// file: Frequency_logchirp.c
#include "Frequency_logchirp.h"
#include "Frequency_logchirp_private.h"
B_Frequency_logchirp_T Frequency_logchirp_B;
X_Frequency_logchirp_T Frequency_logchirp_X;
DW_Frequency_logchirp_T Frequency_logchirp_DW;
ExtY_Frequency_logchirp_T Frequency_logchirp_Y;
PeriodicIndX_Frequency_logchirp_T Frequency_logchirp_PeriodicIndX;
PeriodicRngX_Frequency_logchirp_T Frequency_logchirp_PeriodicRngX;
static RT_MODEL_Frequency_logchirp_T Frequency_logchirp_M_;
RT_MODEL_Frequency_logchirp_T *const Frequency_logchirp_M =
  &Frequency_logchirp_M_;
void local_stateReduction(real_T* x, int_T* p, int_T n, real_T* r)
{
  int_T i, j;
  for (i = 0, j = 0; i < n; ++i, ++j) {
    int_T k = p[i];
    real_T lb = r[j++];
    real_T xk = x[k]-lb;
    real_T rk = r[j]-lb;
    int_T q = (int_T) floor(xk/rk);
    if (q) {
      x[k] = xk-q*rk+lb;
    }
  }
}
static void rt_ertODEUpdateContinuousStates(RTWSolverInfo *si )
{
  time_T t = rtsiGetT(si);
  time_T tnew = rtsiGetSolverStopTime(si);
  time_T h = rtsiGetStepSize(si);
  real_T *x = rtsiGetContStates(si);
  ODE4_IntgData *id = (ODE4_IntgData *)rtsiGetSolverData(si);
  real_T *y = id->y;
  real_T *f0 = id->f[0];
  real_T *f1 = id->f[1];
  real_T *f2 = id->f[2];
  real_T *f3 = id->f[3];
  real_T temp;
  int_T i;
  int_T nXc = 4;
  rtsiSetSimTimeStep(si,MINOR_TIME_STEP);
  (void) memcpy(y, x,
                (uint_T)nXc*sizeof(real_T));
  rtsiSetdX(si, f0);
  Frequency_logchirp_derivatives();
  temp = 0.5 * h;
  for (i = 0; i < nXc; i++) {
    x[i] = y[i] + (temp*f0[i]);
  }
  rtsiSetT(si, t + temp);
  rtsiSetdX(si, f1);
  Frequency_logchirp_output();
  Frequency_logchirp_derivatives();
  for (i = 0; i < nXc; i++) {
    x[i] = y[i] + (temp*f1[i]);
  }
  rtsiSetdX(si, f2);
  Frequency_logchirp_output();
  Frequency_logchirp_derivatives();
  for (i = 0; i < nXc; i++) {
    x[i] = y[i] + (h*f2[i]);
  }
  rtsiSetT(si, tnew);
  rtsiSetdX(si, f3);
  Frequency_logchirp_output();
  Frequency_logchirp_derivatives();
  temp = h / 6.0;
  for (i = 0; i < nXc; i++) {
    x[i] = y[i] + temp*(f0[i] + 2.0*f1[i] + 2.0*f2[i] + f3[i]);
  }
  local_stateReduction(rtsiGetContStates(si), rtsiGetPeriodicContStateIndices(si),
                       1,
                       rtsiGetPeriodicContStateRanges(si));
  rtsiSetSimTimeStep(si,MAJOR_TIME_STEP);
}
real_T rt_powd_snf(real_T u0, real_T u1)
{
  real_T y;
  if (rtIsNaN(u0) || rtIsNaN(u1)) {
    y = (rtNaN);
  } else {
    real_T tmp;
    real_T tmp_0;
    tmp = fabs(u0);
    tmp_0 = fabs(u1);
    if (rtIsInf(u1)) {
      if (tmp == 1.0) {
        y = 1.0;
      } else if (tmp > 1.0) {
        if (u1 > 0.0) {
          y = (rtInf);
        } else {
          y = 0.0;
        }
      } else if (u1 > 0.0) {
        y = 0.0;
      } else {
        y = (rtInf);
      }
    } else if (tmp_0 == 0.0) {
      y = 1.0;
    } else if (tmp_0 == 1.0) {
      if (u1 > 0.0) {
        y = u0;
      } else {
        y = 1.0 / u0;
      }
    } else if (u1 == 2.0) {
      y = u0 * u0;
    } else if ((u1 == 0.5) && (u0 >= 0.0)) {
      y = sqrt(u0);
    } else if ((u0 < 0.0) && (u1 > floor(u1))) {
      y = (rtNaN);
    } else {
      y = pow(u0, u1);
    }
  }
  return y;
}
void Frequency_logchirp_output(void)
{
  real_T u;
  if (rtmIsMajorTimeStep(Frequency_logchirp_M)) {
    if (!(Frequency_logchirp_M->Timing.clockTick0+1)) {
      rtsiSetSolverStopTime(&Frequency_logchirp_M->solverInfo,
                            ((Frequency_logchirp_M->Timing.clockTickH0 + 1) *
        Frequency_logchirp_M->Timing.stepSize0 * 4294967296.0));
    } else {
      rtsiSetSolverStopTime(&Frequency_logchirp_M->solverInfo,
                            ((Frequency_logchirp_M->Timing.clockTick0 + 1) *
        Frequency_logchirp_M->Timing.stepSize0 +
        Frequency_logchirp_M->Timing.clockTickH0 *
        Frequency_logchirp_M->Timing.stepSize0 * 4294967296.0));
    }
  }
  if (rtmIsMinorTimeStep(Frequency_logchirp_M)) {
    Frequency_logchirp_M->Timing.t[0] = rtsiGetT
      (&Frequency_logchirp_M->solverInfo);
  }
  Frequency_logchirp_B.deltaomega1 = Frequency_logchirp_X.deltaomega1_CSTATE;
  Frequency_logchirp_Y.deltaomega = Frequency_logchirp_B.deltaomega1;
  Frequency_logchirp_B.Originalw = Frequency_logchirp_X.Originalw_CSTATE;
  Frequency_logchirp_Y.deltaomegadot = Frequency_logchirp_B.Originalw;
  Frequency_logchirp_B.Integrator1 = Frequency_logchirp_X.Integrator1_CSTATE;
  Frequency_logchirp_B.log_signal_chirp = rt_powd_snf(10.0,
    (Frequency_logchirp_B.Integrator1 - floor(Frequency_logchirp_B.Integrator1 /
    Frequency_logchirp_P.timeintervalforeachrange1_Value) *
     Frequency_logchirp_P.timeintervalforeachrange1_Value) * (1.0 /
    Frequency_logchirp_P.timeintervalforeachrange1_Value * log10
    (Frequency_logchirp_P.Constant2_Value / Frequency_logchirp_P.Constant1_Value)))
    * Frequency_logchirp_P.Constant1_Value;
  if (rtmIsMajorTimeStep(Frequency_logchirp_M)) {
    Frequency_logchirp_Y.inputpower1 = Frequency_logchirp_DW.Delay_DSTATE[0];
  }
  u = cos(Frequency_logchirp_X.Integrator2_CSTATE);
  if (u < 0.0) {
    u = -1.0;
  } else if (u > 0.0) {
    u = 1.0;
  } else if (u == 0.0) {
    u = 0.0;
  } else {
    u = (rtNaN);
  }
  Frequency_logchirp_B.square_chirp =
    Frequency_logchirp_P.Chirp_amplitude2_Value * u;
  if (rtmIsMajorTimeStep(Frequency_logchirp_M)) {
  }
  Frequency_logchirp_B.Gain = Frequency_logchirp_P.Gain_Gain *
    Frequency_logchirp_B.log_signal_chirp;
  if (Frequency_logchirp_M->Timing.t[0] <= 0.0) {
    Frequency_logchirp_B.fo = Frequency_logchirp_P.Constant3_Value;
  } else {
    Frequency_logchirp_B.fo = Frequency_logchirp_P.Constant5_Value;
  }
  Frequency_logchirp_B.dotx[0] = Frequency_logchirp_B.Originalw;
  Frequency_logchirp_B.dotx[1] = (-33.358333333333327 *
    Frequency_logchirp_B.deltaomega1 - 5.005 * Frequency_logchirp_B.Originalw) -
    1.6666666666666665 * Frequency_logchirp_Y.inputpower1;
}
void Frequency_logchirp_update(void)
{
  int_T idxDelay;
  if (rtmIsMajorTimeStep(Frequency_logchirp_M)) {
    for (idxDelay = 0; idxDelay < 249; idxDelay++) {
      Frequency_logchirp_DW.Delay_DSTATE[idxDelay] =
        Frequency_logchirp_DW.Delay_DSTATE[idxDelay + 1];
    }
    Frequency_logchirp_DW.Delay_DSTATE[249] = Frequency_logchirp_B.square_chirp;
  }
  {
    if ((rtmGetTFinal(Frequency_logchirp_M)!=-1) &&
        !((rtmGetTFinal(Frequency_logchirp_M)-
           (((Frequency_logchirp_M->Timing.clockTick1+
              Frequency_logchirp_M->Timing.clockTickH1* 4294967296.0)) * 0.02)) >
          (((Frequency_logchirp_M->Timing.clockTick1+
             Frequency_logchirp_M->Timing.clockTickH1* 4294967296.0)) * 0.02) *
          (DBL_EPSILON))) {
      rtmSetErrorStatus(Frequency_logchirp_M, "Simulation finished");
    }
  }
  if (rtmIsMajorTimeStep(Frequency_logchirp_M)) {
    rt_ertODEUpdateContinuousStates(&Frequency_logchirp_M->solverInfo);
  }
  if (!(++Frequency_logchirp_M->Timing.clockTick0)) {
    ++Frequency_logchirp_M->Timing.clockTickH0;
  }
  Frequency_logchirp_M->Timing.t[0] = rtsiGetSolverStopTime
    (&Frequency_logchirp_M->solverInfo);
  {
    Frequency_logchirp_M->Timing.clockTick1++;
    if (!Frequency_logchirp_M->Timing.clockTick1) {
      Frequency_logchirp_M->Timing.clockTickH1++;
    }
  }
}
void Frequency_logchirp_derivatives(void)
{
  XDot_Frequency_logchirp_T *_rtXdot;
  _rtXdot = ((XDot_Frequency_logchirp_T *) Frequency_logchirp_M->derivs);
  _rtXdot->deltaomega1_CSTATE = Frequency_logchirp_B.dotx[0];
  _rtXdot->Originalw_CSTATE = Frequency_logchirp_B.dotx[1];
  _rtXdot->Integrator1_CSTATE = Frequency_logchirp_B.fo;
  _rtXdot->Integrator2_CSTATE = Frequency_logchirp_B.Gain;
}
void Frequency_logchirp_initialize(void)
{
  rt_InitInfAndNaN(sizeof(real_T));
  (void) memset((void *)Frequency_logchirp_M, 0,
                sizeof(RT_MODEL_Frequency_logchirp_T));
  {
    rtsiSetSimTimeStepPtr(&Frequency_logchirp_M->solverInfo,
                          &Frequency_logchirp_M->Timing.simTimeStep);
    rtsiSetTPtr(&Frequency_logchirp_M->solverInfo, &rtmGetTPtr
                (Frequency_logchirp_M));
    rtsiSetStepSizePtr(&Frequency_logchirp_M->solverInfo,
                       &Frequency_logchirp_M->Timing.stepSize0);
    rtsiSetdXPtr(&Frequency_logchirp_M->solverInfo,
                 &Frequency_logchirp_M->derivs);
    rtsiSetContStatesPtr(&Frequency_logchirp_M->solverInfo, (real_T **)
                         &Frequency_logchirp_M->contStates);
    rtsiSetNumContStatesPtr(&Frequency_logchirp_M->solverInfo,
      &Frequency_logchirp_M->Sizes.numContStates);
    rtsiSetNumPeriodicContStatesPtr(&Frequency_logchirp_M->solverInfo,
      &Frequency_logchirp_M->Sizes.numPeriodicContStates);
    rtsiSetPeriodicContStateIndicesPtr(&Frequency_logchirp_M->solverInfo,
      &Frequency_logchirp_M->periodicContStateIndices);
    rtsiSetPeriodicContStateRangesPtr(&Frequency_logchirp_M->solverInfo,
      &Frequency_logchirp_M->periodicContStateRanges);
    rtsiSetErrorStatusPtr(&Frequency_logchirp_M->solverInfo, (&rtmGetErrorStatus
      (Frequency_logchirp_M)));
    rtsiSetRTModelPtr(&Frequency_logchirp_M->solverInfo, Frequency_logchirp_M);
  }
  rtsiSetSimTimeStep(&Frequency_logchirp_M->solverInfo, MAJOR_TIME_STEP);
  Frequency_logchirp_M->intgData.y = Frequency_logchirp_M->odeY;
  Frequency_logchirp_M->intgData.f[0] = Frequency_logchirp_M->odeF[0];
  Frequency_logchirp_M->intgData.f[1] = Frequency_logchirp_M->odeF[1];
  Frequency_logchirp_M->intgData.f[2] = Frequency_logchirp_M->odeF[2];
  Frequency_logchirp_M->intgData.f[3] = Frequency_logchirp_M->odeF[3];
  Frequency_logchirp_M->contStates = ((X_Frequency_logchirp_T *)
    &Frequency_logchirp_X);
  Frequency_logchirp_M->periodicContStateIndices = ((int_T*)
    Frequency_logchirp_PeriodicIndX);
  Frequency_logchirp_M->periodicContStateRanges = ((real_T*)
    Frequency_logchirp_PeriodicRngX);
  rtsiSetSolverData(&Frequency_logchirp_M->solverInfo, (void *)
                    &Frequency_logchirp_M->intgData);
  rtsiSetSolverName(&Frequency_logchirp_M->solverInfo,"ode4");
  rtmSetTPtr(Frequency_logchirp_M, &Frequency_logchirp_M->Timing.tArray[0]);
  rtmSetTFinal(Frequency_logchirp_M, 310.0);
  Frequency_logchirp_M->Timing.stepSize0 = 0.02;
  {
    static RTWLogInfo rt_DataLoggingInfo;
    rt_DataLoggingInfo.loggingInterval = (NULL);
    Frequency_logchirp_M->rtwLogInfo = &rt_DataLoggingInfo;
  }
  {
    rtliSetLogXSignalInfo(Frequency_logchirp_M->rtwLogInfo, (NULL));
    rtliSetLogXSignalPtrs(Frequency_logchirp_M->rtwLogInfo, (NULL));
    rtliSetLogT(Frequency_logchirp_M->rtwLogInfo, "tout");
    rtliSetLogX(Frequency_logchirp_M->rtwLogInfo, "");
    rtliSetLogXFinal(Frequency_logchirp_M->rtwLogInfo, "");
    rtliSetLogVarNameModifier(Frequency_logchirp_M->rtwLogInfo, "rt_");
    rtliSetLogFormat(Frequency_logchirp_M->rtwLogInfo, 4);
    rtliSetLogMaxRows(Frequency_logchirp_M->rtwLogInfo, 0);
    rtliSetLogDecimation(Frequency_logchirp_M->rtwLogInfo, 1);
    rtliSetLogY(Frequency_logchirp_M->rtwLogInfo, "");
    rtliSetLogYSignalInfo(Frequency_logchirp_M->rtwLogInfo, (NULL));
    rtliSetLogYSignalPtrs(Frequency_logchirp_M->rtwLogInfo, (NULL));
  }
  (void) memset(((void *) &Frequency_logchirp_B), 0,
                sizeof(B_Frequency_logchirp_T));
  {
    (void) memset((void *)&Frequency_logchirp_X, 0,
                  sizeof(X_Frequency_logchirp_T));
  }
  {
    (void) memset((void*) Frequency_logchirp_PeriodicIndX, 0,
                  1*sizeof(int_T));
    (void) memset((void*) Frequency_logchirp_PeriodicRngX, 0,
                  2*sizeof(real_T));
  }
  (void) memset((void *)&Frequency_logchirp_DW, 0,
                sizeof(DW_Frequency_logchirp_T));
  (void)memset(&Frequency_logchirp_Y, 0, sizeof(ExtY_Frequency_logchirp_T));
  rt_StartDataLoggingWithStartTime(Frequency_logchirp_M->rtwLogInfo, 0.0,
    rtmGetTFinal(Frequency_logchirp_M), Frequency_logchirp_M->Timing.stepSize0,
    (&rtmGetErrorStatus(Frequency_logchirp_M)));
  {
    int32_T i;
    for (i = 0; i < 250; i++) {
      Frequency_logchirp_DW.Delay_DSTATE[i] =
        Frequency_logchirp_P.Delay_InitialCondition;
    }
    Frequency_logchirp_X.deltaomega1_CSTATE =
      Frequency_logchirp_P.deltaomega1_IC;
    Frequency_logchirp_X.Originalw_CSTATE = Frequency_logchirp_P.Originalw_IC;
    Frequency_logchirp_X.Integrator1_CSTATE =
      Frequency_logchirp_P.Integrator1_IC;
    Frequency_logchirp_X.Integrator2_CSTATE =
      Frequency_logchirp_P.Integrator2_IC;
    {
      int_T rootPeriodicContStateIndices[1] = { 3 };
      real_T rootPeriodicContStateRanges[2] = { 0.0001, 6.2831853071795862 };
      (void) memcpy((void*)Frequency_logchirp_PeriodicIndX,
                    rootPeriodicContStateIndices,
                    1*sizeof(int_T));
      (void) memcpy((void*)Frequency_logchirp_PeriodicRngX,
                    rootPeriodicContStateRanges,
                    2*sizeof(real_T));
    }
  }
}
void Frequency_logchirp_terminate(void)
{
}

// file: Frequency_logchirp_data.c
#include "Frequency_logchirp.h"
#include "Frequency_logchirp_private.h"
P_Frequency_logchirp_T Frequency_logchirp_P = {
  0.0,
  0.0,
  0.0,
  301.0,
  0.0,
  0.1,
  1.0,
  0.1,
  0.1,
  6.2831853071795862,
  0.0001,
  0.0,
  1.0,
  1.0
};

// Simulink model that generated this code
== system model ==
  inputpower1 : Outport  <- 1: Delay
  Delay : Delay  DelayLength=250  <- 1: MATLABFunction#1
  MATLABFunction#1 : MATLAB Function  <- 1: Chirp_amplitude2, 2: Integrator2
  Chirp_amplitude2 : Constant  Value=0.1
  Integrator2 : Integrator  InitialCondition=0.1  <- 1: Gain
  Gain : Gain  <- 1: MATLABFunction#2
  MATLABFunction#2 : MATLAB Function  <- 1: timeintervalforeachrange1, 2: Integrator1, 3: Constant1, 4: Constant2
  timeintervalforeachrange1 : Constant  Value=301
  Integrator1 : Integrator  <- 1: MATLABFunction#3
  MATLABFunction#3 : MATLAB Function  <- 1: Constant5, 2: Constant3, 3: Clock#1
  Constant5 : Constant
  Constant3 : Constant  Value=0
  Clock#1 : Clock
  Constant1 : Constant  Value=0.1
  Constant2 : Constant
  deltaomega : Outport  <- 1: deltaomega1
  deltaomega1 : Integrator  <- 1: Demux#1
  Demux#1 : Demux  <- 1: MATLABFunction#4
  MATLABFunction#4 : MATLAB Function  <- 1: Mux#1, 2: Delay
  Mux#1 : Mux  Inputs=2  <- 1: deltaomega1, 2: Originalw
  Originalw : Integrator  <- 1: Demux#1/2
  deltaomegadot : Outport  <- 1: Originalw
== matlab function MATLABFunction#2 ==
function log_signal_chirp = fcn(T,t, fmin, fmax)
k = floor(t/T);
f0 = fmin;
f1 = fmax;
lambda1 = 1/T * log10(f1 / f0);

log_signal_chirp = f0*(10^(lambda1*(t-k*T)));

== matlab function MATLABFunction#4 ==
function dotx  = fcn(x, u)
D = 1.5/100;
M = 3.0;
    Tg = 0.2;
    Rp = 0.05;
    Ki=2;
    dotx = zeros(2, 1);
    %x1 = x(1);
    x1 = x(1);
    x2=x(2);
    dotx = [x2;-(D/(M*Tg)+1/(Rp*M*Tg))*x1-(D/M+1/Tg)*x2-1/(M*Tg)*u];

== matlab function MATLABFunction#3 ==
function fo   = signal_generator(step_signal,constant_signal,t)

if t <= 0
    fo = constant_signal;
else
    fo = step_signal;
end
